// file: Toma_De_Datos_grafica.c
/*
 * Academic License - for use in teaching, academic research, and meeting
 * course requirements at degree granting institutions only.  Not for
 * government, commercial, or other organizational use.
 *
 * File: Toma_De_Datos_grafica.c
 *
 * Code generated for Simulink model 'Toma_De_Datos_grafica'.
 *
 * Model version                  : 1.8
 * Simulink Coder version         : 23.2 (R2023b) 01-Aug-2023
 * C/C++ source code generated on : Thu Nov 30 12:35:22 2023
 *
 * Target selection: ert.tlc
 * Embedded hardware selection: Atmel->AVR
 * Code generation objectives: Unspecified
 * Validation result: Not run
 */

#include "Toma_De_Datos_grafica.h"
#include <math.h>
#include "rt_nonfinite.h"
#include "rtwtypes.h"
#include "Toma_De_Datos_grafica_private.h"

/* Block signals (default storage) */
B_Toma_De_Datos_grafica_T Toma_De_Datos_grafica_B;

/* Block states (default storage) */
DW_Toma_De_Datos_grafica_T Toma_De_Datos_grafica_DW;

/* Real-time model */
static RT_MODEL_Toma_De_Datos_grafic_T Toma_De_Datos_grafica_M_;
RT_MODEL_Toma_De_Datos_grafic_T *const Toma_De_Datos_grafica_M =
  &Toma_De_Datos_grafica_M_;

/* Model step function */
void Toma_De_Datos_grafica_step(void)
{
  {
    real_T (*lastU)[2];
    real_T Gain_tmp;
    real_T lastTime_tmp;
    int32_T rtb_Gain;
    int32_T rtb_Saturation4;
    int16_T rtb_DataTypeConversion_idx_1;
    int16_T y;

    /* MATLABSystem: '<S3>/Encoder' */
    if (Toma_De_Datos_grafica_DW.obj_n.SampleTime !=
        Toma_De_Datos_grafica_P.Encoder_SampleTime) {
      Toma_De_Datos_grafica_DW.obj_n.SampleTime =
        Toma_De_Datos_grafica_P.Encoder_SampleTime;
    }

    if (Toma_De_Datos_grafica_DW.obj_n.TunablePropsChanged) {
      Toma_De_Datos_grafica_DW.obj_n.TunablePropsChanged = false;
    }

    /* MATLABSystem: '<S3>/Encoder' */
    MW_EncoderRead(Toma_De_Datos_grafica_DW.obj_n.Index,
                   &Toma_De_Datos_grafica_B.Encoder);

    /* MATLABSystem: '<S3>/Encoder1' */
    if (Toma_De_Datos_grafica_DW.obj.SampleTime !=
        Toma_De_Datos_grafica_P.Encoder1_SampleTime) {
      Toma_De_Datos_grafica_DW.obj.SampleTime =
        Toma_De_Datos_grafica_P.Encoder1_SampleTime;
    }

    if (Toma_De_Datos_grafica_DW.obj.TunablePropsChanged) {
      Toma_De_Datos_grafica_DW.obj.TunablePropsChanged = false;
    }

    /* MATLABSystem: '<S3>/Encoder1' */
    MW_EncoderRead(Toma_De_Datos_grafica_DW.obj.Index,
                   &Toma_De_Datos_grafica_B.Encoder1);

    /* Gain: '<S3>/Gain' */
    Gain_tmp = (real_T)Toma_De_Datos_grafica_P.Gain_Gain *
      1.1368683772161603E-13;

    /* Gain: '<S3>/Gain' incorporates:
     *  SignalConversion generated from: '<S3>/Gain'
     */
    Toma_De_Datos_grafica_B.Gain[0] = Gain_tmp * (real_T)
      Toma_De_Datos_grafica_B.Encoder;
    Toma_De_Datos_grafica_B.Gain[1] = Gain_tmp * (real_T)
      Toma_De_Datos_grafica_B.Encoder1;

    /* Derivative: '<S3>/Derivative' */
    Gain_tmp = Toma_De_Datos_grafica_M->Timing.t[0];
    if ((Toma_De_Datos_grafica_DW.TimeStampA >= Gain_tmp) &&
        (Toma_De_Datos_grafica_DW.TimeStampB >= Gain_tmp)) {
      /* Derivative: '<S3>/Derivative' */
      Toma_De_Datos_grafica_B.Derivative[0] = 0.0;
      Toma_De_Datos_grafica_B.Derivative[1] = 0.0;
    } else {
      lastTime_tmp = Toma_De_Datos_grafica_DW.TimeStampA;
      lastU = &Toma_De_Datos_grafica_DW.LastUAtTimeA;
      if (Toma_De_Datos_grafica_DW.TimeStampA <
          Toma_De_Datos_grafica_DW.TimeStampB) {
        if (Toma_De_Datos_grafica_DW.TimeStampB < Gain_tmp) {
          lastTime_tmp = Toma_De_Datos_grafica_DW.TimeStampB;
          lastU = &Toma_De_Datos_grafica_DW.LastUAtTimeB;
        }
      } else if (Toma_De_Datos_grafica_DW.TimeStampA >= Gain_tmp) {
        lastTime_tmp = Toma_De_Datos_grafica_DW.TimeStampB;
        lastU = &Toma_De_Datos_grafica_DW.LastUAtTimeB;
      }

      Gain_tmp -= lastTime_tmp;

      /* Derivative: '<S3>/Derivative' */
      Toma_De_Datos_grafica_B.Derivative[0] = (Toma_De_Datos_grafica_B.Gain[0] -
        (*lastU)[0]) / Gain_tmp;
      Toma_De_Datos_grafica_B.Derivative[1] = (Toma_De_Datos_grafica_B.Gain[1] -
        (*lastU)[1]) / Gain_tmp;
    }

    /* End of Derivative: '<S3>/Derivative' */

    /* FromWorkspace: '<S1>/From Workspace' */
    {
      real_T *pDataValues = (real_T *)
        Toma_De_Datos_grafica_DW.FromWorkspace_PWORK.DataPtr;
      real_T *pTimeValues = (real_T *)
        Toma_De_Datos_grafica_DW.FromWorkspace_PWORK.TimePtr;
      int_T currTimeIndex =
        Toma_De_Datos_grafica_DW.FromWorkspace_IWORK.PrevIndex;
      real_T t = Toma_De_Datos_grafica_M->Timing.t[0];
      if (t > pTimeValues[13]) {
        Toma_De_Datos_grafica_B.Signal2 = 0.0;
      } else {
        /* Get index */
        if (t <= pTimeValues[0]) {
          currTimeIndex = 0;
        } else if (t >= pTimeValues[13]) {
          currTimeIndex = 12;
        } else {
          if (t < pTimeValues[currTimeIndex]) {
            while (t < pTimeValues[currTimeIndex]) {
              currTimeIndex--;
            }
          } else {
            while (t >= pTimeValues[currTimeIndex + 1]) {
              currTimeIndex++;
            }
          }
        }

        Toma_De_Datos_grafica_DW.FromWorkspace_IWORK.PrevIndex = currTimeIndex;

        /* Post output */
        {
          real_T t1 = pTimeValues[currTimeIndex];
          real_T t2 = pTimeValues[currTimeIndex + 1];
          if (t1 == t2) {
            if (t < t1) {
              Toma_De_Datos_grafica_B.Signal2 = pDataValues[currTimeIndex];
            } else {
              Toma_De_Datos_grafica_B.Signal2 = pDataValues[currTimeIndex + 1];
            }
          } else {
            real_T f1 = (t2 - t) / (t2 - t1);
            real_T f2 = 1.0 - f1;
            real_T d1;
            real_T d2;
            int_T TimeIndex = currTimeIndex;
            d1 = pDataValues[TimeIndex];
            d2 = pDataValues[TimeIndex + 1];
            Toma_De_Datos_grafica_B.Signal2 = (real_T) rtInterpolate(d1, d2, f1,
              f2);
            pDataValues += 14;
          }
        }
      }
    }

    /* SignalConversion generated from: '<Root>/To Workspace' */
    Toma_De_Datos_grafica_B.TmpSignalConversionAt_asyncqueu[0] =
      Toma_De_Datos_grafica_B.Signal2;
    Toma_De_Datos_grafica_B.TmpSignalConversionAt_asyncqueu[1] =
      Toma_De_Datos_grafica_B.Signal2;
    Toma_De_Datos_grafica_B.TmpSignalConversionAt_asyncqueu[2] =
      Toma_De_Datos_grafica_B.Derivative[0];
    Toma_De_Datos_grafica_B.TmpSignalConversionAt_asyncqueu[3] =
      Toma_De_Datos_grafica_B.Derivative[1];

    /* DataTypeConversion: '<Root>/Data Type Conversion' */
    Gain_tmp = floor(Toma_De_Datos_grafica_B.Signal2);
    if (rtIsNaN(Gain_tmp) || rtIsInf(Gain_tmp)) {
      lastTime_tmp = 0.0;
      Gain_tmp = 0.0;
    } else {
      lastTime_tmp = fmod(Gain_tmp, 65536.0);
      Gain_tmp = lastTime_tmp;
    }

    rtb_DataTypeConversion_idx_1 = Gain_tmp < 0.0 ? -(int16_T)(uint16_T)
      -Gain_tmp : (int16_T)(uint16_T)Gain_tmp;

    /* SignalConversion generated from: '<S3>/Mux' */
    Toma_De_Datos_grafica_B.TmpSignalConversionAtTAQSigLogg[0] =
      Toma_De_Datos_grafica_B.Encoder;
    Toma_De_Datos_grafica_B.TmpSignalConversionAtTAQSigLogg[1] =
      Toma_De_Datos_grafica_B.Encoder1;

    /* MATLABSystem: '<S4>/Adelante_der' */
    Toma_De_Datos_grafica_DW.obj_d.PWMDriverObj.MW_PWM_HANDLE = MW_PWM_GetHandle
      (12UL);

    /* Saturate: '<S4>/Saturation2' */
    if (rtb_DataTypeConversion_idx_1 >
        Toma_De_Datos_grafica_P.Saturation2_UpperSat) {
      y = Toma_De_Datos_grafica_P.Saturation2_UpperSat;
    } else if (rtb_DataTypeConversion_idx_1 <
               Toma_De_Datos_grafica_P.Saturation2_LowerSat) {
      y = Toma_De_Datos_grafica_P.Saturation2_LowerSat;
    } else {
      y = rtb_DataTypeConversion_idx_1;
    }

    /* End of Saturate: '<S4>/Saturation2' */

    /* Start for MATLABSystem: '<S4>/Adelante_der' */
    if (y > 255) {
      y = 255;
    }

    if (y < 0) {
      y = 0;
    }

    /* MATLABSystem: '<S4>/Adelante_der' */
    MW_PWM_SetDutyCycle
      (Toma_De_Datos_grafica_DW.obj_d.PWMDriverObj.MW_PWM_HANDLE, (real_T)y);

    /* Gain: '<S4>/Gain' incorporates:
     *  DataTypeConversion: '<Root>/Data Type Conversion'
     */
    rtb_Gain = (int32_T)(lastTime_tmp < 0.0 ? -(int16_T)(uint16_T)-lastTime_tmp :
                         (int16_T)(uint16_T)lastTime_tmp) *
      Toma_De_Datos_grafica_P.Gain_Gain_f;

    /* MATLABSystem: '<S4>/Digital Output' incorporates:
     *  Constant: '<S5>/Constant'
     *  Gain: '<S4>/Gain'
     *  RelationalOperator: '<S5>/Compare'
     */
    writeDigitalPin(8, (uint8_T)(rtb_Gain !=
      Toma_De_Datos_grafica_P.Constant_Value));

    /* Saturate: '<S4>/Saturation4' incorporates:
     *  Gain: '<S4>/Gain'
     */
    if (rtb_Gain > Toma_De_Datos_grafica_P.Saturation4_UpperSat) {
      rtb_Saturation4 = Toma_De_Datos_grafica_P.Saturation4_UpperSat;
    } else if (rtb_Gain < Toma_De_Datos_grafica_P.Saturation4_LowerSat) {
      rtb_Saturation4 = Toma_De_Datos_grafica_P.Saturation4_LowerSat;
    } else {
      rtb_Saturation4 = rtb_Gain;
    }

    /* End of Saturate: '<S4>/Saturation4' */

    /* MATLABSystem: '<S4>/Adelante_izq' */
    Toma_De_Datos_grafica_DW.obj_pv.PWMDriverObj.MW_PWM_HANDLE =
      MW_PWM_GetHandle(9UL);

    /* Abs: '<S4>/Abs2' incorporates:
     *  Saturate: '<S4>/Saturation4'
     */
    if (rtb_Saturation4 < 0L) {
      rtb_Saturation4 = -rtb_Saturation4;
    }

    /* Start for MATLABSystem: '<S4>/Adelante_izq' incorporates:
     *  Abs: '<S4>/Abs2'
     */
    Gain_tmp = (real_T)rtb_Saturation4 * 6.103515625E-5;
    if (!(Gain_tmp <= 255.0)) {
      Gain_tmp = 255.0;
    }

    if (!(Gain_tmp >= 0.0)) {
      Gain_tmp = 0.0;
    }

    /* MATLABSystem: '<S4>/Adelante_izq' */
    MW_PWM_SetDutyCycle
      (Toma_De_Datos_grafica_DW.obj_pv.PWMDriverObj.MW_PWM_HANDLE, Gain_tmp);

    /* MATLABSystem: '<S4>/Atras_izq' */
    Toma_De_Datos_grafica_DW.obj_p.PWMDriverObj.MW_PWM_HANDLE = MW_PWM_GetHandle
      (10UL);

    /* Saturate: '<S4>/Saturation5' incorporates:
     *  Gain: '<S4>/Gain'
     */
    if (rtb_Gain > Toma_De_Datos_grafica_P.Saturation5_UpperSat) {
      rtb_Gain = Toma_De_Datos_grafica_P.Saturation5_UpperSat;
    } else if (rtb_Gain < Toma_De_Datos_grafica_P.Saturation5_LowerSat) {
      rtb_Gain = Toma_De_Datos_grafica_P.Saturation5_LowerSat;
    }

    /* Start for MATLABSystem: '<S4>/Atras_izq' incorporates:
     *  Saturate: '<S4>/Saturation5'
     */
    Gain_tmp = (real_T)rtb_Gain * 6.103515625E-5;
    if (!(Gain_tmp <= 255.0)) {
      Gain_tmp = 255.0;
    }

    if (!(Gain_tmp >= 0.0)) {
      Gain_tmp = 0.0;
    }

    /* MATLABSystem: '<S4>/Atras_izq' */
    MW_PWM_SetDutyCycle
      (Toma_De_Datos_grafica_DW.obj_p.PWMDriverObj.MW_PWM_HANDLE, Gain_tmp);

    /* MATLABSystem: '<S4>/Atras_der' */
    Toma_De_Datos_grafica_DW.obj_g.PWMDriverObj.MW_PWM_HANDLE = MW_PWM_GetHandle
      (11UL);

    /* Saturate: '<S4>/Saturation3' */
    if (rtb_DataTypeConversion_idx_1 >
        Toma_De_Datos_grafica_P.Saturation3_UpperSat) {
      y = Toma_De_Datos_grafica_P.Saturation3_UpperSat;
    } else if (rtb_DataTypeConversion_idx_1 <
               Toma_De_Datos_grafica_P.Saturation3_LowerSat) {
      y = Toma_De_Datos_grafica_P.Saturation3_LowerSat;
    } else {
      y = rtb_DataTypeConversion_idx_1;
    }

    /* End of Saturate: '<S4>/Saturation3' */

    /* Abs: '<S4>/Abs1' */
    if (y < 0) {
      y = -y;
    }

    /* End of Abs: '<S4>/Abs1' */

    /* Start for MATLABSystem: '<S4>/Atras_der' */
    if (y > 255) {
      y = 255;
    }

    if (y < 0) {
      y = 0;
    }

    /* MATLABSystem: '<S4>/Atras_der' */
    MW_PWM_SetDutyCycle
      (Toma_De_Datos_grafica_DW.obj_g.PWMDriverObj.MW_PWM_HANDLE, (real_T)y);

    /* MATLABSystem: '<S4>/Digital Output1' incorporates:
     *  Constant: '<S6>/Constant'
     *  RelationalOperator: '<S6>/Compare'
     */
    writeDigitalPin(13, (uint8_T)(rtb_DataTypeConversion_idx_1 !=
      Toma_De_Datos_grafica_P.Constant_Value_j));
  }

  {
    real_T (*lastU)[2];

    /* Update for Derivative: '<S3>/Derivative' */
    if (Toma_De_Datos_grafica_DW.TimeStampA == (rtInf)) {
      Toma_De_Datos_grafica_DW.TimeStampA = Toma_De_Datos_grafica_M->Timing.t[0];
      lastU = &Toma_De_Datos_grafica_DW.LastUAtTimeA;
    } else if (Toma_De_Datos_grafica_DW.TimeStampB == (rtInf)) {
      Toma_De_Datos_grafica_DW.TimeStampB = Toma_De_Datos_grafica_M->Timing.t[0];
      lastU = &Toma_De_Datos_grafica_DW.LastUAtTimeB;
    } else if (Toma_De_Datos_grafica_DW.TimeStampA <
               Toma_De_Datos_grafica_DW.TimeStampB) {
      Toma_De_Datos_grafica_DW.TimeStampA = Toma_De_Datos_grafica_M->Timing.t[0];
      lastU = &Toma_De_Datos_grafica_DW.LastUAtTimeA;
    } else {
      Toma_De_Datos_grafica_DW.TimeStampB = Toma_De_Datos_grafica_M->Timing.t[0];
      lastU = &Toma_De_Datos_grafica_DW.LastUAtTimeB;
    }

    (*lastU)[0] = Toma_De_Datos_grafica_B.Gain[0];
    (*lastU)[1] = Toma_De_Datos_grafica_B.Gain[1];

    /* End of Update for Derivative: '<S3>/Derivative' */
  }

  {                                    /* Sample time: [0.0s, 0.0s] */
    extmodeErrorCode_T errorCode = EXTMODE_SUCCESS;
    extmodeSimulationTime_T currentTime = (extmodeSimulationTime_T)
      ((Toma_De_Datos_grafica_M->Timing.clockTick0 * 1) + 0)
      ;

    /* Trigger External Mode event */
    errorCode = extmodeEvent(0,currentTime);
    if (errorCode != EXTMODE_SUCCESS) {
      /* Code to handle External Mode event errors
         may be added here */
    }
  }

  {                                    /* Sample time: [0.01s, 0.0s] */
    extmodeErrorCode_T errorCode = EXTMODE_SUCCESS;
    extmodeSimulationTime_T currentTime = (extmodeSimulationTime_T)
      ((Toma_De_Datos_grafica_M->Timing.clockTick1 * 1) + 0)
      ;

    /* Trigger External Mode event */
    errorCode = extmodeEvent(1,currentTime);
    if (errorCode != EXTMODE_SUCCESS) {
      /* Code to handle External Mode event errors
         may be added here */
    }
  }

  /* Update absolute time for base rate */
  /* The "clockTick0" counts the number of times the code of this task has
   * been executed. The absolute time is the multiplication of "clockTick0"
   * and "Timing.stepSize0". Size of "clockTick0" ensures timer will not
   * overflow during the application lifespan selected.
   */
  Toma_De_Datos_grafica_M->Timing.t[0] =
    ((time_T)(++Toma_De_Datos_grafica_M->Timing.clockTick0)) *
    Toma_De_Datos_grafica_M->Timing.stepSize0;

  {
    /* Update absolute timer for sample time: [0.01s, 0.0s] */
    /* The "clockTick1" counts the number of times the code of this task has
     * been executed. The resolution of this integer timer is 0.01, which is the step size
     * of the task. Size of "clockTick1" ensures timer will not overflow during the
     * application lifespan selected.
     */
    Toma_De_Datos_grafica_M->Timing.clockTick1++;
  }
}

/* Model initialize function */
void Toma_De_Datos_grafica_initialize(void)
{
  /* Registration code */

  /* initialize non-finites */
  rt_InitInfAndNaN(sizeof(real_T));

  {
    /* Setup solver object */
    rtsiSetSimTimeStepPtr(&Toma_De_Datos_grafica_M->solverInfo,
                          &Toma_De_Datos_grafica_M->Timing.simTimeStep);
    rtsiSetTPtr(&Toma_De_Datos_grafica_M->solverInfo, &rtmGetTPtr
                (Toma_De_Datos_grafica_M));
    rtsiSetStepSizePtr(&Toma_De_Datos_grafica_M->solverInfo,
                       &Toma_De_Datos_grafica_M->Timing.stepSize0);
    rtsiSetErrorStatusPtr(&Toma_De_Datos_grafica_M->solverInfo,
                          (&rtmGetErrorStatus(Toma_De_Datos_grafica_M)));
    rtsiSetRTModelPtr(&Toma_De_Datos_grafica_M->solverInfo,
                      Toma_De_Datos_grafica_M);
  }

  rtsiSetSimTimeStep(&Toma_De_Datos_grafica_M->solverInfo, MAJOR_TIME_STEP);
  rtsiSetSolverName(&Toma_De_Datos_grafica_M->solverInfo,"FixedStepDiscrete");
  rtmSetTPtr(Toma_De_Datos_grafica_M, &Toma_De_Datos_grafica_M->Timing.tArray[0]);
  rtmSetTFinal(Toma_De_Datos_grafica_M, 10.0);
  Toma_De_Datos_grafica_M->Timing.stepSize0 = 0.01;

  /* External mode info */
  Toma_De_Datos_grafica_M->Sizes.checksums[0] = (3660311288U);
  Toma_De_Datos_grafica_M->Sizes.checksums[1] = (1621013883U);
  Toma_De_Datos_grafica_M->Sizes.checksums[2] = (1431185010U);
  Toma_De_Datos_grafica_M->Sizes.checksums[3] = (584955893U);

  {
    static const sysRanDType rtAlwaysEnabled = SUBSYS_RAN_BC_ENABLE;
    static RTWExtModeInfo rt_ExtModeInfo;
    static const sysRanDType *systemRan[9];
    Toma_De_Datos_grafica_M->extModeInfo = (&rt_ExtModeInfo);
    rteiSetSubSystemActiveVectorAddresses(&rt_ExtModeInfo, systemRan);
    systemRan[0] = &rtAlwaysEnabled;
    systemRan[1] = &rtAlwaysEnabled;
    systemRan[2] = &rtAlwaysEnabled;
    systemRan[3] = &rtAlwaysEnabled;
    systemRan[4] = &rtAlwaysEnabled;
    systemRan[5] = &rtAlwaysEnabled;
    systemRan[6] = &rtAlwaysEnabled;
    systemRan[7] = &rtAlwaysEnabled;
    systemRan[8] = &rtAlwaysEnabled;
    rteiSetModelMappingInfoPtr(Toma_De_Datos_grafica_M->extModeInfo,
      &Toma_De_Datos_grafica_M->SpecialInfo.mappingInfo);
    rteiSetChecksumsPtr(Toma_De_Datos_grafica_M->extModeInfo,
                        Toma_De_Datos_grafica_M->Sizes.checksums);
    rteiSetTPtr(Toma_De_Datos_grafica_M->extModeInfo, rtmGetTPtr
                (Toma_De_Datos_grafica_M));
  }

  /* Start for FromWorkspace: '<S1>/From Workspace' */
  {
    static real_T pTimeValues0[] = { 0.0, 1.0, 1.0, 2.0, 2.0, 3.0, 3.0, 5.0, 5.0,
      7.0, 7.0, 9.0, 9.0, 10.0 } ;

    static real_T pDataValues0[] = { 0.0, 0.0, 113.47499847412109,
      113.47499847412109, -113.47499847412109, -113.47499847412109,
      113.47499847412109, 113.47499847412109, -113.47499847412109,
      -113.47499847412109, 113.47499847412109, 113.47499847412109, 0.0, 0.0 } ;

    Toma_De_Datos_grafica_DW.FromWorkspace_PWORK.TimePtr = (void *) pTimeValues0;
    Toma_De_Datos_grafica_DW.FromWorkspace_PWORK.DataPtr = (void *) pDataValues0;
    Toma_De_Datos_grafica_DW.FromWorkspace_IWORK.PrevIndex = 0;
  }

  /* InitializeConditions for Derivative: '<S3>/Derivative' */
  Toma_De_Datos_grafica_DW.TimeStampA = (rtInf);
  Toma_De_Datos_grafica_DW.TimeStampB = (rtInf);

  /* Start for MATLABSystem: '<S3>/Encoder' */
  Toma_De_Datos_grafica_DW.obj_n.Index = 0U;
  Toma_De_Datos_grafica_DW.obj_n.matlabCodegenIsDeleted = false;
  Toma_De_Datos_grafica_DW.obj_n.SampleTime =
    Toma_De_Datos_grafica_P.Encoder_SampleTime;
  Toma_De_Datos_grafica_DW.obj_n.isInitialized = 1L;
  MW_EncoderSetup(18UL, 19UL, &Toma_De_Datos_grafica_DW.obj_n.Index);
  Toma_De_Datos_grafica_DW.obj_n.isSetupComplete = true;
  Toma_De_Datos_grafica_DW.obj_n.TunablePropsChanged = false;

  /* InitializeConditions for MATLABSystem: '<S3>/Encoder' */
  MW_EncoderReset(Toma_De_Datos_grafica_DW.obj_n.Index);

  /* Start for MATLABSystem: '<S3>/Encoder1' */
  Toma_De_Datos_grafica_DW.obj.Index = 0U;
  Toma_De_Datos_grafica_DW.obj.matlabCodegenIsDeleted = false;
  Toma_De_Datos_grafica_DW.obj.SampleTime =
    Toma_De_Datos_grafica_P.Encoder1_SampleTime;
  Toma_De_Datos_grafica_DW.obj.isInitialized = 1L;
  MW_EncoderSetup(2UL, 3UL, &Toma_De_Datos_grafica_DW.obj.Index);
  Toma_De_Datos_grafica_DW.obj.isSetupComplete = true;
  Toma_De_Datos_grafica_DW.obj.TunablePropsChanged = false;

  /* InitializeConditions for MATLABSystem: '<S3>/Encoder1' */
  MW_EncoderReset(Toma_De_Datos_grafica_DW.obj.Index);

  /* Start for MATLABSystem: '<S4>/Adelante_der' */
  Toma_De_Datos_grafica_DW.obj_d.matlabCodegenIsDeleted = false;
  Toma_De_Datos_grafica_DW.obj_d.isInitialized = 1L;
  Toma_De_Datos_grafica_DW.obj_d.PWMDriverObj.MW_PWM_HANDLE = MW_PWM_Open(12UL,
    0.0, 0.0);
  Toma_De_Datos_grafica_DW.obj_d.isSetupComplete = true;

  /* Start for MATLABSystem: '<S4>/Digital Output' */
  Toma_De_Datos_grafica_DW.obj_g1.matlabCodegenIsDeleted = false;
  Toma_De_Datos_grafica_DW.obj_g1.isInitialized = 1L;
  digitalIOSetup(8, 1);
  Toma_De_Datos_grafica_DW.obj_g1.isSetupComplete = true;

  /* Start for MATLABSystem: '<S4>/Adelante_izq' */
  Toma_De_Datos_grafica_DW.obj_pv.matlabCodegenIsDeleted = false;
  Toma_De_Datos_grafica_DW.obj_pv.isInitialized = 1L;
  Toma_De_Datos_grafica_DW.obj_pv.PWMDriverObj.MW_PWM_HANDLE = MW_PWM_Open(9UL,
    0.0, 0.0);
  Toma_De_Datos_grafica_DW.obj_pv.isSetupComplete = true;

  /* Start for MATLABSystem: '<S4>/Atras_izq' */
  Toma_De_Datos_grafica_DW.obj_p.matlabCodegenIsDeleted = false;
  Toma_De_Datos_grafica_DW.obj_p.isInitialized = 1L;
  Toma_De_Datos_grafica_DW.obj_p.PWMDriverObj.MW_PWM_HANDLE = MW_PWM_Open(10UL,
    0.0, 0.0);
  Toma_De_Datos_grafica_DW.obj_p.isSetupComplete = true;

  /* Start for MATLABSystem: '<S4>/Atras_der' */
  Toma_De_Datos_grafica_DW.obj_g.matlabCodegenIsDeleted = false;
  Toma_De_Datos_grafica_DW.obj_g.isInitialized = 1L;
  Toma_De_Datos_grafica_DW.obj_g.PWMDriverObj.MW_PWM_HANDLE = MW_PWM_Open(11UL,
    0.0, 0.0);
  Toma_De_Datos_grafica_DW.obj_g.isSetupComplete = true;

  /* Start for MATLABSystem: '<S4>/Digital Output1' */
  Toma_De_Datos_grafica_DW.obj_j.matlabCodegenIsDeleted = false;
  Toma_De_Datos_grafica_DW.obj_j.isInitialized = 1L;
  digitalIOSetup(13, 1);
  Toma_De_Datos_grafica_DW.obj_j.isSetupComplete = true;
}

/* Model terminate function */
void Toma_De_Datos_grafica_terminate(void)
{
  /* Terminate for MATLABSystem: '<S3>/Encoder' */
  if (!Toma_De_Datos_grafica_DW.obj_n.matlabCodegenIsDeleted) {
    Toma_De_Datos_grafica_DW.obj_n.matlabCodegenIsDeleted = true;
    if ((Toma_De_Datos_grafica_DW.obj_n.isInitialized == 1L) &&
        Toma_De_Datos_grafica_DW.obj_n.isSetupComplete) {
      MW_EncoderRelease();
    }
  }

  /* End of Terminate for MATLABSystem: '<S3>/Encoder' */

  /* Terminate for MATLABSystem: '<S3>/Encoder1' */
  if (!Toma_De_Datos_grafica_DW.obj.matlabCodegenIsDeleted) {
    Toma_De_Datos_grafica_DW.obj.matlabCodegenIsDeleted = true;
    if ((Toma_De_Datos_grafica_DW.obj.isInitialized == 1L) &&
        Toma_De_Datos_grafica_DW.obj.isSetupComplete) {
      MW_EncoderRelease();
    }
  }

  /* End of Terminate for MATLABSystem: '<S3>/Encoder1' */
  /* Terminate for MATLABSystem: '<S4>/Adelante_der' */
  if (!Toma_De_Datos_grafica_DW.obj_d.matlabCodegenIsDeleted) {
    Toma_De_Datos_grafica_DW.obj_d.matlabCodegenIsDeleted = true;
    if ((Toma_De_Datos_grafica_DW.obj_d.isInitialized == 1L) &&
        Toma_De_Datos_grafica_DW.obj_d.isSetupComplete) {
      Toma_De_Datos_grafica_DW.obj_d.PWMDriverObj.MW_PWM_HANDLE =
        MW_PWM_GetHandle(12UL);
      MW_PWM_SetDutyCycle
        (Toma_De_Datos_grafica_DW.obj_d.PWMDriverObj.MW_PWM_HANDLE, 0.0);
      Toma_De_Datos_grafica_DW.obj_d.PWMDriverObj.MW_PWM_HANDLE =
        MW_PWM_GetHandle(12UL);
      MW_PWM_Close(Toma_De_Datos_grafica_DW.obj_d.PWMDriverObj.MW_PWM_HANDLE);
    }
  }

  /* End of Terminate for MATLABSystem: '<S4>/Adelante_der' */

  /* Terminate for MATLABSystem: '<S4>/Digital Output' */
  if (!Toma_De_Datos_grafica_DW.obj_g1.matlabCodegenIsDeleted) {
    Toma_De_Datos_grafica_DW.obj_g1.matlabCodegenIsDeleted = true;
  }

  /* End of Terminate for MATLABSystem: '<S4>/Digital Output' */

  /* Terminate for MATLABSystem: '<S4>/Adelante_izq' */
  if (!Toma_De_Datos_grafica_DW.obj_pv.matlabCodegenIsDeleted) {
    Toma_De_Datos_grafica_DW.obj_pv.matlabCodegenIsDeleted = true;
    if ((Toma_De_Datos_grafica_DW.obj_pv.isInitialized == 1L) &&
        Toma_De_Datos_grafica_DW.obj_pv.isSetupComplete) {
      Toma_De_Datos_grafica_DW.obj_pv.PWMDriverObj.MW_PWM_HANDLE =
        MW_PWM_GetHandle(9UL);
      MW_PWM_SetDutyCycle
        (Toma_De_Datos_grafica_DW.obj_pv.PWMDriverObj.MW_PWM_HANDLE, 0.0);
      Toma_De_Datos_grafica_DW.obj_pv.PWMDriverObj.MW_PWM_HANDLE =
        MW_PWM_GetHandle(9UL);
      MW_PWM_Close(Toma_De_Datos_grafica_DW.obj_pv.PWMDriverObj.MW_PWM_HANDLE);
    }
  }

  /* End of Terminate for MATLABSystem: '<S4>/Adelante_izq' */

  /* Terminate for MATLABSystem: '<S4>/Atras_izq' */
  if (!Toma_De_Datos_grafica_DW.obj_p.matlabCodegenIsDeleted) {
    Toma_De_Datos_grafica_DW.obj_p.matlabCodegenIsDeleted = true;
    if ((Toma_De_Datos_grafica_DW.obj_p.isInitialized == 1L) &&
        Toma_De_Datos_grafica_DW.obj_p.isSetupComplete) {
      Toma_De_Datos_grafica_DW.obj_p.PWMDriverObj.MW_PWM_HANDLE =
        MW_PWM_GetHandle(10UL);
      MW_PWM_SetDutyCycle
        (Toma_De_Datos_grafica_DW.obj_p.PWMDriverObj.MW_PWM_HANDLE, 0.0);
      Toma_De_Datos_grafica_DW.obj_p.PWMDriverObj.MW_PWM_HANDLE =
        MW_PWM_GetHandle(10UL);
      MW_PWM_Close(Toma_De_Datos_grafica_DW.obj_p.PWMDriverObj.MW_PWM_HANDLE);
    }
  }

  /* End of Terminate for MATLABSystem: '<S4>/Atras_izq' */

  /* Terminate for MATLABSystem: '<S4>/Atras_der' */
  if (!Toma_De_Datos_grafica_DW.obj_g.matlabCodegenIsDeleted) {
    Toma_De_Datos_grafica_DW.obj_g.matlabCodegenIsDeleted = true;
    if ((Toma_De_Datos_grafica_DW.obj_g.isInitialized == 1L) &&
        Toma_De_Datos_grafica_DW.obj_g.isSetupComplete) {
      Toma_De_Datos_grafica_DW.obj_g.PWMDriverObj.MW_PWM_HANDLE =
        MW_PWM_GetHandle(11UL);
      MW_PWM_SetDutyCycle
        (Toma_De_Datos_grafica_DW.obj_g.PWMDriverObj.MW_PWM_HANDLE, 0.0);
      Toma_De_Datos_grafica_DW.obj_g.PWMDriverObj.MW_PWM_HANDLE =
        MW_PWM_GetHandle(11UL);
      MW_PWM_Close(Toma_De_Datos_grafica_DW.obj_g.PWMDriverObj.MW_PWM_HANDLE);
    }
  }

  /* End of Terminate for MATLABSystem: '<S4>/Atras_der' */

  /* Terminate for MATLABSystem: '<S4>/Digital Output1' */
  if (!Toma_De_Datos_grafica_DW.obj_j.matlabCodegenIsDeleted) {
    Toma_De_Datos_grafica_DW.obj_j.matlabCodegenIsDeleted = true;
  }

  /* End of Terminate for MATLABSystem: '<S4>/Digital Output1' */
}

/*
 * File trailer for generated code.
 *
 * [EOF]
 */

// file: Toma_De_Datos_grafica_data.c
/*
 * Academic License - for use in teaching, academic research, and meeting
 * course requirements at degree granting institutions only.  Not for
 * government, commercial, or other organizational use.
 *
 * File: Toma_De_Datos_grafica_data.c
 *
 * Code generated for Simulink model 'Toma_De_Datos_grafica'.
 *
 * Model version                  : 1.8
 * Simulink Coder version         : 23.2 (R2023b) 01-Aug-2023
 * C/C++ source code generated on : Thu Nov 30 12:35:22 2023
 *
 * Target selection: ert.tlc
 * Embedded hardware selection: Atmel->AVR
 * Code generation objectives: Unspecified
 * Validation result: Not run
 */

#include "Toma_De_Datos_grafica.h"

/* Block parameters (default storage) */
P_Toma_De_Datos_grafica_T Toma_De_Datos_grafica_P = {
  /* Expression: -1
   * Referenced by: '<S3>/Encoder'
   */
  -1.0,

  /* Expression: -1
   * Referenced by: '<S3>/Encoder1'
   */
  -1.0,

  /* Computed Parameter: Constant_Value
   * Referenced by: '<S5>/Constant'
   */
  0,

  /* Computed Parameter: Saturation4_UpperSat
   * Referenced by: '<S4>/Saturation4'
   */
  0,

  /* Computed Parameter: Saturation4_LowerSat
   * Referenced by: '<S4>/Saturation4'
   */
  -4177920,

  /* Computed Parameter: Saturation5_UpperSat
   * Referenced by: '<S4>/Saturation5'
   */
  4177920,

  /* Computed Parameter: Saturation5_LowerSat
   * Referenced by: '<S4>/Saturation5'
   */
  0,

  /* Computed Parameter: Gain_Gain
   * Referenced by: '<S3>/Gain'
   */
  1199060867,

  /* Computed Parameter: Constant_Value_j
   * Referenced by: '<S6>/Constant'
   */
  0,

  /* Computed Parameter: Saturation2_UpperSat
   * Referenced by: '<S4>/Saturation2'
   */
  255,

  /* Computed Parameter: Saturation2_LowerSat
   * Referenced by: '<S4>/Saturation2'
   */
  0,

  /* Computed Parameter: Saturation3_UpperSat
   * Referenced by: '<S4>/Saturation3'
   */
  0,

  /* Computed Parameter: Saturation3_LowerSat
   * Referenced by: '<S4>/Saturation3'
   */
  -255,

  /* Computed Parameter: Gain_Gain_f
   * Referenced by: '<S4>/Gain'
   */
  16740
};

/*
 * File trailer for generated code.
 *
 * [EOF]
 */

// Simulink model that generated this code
simulink model "Toma_De_Datos_grafica"  (R2023b)
settings: Solver=FixedStepAuto  StartTime=0.0  StopTime=10  FixedStep=0.01  RelTol=1e-3  EnableMultiTasking=on
libraries: SignalEditorBlockLib x1

== system Toma_De_Datos_grafica ==
  Data Type Conversion : DataTypeConversion  OutDataTypeStr=int16  SaturateOnIntegerOverflow=off  RndMeth=Floor
  Mux : Mux  Inputs=2
  Mux1 : Mux  Inputs=2
  Scope : Scope  NumInputPorts=2
  Signal Editor1 : SignalEditorBlockLib/Signal Editor  FileName=Señal_tiempos.mat  ActiveScenario=Scenario  ActiveSignal=Signal 1  IsBus=off  OutputBusObjectStr=Bus: BusObject  SampleTime=0  OutputAfterFinalValue=Setting to zero  Unit=inherit  PreserveSignalName=on  ApplySigPropsToAllScenarios=on  ApplySigPropsToAllSignals=on
  Subsystem Reference : Subsystem  ReferencedSubsystem=Piero_Hardware
  To Workspace : ToWorkspace  VariableName=simout  SampleTime=-1
  wires:
  Signal Editor1/1 -> Scope/2, Mux/1, Mux/2
  Mux/1 -> Mux1/1, Data Type Conversion/1
  Data Type Conversion/1 -> Subsystem Reference/1
  Subsystem Reference/1 -> Mux1/2, Scope/1
  Mux1/1 -> To Workspace/1
